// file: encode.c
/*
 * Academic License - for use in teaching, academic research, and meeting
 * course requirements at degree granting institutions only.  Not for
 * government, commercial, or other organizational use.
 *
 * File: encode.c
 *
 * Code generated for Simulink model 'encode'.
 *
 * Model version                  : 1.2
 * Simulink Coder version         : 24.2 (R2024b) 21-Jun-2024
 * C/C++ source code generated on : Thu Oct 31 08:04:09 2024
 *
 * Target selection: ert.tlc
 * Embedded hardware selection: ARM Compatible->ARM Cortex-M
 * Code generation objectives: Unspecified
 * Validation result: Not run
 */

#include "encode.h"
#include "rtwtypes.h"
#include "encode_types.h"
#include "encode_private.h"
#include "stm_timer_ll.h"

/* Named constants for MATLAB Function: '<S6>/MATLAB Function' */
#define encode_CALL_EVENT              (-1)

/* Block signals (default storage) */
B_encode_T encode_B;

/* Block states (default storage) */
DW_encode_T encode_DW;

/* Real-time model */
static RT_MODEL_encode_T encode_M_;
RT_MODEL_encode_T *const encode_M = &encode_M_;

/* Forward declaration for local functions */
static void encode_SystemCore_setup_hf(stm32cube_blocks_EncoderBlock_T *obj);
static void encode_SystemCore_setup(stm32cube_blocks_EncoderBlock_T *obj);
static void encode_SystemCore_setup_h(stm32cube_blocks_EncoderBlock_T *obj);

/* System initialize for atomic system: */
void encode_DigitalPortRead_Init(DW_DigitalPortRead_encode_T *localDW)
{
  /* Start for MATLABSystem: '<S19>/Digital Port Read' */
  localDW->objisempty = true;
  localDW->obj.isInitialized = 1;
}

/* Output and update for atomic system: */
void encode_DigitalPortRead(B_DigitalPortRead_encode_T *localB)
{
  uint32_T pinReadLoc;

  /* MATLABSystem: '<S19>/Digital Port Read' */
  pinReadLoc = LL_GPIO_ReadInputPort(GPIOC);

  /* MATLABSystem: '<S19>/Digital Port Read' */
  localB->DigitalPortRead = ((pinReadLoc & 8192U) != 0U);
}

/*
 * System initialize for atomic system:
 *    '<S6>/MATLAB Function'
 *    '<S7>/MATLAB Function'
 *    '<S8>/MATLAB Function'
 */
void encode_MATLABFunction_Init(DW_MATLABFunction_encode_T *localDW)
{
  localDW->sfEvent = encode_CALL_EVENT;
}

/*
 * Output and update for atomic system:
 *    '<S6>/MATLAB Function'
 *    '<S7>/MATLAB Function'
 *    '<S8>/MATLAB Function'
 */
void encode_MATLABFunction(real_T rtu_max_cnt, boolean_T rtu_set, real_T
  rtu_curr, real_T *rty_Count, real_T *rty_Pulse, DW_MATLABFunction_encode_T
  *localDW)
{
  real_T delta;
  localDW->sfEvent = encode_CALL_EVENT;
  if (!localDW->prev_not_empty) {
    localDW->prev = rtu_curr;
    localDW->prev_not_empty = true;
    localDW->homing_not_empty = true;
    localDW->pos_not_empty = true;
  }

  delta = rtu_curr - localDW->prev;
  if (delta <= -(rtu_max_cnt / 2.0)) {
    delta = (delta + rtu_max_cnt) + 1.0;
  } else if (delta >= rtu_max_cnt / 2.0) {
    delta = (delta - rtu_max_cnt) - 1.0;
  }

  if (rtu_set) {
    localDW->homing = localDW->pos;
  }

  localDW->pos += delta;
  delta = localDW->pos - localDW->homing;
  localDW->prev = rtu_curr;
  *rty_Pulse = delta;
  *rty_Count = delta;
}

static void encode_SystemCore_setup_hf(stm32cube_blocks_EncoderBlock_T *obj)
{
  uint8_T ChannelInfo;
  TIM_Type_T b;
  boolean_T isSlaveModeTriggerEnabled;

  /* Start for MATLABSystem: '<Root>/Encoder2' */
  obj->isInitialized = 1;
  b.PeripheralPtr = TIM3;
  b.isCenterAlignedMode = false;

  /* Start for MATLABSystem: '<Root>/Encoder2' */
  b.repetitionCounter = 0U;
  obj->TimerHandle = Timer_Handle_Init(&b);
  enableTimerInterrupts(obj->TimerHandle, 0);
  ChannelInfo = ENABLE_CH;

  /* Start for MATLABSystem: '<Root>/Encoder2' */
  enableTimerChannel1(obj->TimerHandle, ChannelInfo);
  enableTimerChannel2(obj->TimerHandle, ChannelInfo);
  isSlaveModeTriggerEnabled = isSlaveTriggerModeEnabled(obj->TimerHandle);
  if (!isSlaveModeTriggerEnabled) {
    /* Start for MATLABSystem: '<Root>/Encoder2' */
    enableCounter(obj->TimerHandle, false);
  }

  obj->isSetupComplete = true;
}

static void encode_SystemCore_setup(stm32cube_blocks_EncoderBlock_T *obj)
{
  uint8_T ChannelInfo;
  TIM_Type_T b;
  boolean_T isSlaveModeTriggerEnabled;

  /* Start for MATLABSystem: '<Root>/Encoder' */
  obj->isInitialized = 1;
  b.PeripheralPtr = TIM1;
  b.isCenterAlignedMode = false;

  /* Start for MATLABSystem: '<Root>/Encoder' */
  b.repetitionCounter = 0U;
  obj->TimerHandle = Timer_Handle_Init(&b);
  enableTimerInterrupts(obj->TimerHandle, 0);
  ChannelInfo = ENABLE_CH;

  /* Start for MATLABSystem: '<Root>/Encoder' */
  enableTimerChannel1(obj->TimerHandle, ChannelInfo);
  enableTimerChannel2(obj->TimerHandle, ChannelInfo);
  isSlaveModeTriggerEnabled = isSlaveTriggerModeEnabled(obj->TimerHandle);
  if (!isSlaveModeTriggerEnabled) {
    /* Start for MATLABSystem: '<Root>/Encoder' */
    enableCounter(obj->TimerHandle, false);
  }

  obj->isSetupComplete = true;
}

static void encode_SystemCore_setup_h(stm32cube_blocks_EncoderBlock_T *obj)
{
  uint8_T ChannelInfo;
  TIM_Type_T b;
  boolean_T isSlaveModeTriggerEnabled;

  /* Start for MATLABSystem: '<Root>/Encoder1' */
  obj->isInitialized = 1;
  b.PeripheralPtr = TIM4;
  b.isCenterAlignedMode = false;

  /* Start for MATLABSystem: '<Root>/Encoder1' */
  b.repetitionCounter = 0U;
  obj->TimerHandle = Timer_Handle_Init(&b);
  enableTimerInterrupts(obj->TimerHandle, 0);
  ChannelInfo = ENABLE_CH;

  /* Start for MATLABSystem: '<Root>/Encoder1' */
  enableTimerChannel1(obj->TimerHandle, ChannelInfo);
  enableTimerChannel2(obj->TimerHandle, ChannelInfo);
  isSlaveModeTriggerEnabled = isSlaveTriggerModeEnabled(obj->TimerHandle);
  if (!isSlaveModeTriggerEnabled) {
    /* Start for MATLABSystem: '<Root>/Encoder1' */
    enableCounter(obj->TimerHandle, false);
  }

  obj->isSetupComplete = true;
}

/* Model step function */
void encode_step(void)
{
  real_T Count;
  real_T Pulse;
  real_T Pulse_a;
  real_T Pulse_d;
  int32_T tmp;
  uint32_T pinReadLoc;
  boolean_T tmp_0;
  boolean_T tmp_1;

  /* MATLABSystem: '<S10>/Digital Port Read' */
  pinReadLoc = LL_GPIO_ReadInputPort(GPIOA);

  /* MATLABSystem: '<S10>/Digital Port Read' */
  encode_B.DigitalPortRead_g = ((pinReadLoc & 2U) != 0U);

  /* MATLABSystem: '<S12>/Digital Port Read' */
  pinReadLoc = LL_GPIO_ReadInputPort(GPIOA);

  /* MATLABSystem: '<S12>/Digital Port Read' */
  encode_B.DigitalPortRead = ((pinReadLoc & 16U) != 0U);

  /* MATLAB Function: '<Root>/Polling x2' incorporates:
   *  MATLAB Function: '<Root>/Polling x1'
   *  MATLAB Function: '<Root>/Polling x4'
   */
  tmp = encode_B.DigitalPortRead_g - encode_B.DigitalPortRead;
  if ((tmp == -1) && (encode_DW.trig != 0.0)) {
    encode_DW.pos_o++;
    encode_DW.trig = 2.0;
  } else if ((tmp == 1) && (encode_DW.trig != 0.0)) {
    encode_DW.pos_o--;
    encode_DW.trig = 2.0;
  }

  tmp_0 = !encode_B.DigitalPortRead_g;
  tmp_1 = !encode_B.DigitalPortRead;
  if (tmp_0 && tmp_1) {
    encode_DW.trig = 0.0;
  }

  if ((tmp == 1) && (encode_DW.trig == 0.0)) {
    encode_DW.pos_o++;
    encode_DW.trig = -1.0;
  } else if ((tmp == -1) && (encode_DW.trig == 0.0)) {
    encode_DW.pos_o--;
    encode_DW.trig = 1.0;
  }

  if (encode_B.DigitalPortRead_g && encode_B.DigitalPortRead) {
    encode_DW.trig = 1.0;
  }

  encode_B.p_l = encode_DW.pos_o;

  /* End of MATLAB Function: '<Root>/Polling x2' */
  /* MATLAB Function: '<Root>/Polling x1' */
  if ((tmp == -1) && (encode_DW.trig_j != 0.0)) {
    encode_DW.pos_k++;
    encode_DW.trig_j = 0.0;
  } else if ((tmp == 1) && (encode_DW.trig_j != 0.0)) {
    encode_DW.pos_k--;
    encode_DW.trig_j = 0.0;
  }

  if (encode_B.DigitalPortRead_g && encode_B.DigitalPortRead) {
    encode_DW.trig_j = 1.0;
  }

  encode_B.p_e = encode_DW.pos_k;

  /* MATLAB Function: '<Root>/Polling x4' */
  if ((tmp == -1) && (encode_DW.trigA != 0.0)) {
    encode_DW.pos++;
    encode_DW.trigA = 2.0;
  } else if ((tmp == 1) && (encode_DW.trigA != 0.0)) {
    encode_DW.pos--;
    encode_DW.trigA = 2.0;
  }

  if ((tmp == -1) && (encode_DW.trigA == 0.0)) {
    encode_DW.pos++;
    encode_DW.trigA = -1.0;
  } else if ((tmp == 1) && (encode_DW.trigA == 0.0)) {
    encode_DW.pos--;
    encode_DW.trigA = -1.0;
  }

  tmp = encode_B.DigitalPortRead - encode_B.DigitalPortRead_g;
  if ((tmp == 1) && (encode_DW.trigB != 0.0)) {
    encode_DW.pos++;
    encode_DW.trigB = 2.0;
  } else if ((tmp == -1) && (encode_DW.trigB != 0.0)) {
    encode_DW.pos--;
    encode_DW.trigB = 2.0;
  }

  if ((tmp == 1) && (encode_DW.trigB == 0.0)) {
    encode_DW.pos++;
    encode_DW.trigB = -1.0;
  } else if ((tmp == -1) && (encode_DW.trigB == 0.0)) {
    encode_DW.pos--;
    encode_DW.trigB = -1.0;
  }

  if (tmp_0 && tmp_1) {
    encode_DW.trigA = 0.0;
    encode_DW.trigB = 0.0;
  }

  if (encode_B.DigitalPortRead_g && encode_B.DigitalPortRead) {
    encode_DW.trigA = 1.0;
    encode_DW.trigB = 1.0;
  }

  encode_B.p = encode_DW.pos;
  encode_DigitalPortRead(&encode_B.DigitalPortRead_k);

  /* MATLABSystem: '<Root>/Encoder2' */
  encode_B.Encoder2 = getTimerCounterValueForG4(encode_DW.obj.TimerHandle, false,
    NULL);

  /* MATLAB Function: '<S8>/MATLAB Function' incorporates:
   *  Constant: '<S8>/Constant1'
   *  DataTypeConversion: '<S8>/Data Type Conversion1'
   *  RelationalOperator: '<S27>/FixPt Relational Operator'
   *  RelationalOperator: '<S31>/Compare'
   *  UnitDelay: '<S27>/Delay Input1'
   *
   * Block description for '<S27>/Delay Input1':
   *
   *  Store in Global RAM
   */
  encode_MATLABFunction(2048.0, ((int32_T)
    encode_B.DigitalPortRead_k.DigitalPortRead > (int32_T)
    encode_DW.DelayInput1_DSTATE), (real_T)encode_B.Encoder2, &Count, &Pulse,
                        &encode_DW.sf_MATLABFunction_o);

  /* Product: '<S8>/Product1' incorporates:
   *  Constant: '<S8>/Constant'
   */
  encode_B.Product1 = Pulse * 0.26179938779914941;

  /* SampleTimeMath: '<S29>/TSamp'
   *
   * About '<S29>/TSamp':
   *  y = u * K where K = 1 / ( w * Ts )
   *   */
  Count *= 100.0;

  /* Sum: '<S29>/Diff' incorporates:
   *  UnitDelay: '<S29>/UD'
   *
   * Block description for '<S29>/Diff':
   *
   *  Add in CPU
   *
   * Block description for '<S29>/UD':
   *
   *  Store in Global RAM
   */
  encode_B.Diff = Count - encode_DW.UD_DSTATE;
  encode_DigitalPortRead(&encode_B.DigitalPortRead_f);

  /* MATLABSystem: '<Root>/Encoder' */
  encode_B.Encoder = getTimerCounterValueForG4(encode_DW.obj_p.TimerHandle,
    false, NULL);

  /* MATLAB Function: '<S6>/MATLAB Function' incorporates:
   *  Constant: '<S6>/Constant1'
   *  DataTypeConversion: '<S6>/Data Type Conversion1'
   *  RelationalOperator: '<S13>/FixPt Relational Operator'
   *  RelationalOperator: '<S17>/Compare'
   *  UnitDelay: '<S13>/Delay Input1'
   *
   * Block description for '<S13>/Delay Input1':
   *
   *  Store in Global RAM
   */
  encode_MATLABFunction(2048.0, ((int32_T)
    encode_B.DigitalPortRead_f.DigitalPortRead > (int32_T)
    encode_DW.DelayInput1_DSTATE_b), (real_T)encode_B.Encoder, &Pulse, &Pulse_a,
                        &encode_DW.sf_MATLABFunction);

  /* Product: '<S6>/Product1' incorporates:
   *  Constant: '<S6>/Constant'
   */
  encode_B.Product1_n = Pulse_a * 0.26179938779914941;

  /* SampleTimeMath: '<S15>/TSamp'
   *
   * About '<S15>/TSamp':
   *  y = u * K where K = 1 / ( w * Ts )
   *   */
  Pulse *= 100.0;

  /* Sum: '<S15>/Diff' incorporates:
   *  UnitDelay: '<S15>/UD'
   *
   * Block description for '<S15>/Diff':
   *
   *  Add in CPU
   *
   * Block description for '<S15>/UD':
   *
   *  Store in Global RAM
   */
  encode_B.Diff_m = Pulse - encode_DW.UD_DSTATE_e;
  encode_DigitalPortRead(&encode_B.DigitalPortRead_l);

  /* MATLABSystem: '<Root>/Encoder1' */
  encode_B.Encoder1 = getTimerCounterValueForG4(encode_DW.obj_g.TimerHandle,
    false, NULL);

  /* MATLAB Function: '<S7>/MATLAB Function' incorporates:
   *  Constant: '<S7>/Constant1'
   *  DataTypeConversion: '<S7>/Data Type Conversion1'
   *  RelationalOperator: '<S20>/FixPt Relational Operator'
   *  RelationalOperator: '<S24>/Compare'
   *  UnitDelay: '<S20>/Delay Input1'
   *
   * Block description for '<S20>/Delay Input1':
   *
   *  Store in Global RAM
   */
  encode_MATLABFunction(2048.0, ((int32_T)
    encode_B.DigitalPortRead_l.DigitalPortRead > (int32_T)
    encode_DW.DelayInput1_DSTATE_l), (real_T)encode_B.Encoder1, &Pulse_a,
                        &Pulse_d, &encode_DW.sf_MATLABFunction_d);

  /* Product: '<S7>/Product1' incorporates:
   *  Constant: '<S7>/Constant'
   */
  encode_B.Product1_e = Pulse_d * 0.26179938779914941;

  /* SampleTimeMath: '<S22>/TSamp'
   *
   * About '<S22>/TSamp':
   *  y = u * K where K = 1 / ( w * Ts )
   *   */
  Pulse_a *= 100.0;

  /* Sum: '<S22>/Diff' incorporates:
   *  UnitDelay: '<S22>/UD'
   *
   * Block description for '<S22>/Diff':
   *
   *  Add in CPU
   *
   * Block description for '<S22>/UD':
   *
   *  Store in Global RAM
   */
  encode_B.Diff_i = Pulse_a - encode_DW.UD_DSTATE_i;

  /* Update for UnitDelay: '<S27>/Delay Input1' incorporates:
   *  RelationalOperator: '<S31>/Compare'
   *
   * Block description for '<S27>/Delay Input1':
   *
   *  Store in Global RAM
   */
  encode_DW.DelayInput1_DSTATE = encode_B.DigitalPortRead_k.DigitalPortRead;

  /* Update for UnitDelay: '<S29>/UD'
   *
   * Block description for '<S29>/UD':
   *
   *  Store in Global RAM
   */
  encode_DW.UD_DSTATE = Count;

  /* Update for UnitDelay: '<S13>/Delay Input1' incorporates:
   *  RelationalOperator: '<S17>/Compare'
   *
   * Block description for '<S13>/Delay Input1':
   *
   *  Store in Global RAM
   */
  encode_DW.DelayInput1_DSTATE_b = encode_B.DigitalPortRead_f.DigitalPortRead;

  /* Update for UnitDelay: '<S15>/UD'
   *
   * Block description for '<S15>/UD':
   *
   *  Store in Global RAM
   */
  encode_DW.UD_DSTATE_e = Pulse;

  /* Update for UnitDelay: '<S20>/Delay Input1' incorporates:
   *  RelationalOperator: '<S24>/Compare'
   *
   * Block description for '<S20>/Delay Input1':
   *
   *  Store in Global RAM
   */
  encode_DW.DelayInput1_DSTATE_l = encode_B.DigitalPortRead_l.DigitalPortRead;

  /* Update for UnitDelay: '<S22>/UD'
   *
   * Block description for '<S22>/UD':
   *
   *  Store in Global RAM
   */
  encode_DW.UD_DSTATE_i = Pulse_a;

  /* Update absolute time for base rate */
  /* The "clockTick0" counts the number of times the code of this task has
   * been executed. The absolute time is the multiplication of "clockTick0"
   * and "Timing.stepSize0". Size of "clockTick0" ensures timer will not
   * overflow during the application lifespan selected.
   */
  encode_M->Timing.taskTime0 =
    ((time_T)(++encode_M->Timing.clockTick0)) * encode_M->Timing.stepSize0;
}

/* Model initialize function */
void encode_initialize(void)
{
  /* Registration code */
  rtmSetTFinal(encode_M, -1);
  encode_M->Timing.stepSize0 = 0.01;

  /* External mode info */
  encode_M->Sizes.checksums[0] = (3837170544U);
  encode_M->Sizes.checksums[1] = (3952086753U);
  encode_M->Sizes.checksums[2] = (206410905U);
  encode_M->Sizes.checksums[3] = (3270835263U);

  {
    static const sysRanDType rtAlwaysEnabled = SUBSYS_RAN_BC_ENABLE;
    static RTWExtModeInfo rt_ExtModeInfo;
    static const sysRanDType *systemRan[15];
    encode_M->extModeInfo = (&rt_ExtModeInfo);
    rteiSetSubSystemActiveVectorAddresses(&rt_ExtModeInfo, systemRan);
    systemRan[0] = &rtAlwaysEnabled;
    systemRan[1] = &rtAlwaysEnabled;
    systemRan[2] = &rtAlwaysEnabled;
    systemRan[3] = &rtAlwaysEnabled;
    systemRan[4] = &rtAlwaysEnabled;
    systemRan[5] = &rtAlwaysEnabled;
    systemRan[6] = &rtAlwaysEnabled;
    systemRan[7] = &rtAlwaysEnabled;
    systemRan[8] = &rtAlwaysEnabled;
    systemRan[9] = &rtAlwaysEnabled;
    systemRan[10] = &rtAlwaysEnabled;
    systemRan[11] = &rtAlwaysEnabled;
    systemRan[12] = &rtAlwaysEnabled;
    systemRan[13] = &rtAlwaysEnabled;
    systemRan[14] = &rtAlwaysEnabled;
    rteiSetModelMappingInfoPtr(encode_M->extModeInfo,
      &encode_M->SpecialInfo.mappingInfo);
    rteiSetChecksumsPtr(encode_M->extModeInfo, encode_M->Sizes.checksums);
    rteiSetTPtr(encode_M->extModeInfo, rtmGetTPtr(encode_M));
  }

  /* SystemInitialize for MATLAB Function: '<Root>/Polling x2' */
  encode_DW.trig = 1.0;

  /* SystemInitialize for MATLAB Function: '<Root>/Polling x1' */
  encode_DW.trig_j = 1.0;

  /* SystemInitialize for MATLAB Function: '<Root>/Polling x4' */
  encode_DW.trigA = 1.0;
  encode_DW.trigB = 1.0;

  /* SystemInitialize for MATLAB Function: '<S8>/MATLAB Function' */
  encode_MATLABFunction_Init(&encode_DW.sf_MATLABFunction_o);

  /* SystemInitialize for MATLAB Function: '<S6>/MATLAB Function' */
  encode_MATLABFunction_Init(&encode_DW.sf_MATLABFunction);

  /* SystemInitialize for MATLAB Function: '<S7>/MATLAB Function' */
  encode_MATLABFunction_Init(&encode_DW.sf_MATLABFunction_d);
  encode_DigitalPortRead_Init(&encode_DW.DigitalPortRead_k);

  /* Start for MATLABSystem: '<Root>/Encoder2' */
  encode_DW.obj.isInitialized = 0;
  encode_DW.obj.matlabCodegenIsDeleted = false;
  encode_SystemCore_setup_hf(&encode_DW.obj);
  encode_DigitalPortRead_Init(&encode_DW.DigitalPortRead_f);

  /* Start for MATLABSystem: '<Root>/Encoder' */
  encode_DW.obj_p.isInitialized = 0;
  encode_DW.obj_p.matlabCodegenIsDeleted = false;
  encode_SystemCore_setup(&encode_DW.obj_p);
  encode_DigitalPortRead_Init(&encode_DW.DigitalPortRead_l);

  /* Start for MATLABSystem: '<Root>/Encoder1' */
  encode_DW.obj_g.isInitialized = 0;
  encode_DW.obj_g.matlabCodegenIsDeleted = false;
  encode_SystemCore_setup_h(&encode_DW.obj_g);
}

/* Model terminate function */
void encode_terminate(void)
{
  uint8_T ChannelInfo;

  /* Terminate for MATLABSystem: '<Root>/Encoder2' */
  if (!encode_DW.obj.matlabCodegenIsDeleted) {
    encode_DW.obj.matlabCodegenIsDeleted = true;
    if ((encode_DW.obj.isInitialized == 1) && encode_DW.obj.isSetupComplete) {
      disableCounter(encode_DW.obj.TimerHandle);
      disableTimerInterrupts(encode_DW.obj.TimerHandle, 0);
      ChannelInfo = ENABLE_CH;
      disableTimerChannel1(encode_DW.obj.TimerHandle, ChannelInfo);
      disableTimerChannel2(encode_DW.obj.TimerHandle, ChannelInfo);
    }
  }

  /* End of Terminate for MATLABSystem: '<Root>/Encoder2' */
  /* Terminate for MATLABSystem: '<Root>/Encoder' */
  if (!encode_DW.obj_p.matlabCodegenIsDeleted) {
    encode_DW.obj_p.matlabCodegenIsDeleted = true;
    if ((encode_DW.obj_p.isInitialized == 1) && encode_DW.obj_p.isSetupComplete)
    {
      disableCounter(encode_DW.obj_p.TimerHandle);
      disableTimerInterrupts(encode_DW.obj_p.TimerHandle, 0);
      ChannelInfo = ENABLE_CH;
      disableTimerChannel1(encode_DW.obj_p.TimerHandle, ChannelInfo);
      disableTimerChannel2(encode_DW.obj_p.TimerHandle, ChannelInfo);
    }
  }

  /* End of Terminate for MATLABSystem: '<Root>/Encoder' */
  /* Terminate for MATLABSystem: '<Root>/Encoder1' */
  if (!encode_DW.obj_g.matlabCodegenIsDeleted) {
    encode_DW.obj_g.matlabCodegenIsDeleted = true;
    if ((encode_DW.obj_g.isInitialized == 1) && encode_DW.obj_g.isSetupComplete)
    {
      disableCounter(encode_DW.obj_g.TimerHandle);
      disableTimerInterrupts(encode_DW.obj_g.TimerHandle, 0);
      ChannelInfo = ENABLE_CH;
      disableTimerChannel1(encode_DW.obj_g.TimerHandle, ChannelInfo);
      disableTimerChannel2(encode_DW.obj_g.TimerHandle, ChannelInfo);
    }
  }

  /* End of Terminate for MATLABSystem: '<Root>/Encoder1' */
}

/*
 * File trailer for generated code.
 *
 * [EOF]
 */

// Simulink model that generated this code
simulink model "encode"  (R2024b)
settings: Solver=FixedStepAuto  StartTime=0.0  StopTime=inf  FixedStep=0.01  RelTol=1e-3  EnableMultiTasking=on
libraries: simulink x6, stm32f4xxblockslib x5, stm32g4xxblockslib x3

== system encode ==
  Display{1..4,6..7,9..10,12} (9 alike) : Display
  Encoder : stm32g4xxblockslib/Encoder  TimerModule=TIM1  EnableResetInput=off  OutputCountAfterFirstIndex=off  OutputValidIndex=off  OutputDirection=off  OutputStatus=off  SampleTime=-1
  Encoder1 : stm32g4xxblockslib/Encoder  TimerModule=TIM4  EnableResetInput=off  OutputCountAfterFirstIndex=off  OutputValidIndex=off  OutputDirection=off  OutputStatus=off  SampleTime=-1
  Encoder2 : stm32g4xxblockslib/Encoder  TimerModule=TIM3  EnableResetInput=off  OutputCountAfterFirstIndex=off  OutputValidIndex=off  OutputDirection=off  OutputStatus=off  SampleTime=-1
  PA1_ReadA : stm32f4xxblockslib/Digital Port Read  PortName=GPIOA  PinNumber=[1]  ReadOperation=on  IOAsArray=on  SampleTime=-1  EnableSimPort=off  hoistedMaskSrc=ECSoC/ECSimCodegen/Digital Port Read
  PA4_ReadB : stm32f4xxblockslib/Digital Port Read  PortName=GPIOA  PinNumber=[4]  ReadOperation=on  IOAsArray=on  SampleTime=-1  EnableSimPort=off  hoistedMaskSrc=ECSoC/ECSimCodegen/Digital Port Read
  Polling x1 : MATLAB Function  TreatAsAtomicUnit=on
  Polling x2 : MATLAB Function  TreatAsAtomicUnit=on
  Polling x4 : MATLAB Function  TreatAsAtomicUnit=on
  QEI x1 : Subsystem
  QEI x2 : Subsystem
  QEI x4 : Subsystem
  wires:
  PA4_ReadB/1 -> Polling x2/2(b), Polling x4/2(b), Polling x1/2(b)
  PA1_ReadA/1 -> Polling x4/1(a), Polling x2/1(a), Polling x1/1(a)
  Encoder/1 -> QEI x1/1(curr)
  QEI x1/1(Velocity) -> Display4/1
  QEI x1/2(Position) -> Display6/1
  QEI x2/2(Position) -> Display9/1
  QEI x2/1(Velocity) -> Display7/1
  Encoder1/1 -> QEI x2/1(curr)
  QEI x4/2(Position) -> Display12/1
  QEI x4/1(Velocity) -> Display10/1
  Encoder2/1 -> QEI x4/1(curr)
  Polling x1/1(p) -> Display2/1
  Polling x2/1(p) -> Display1/1
  Polling x4/1(p) -> Display3/1

== system encode/QEI x1 ==
  curr : Inport
  Constant : Constant  Value=pi/12
  Constant1 : Constant  Value=2048
  Data Type Conversion1 : DataTypeConversion  OutDataTypeStr=double  SaturateOnIntegerOverflow=off  RndMeth=Floor
  Detect Rise Positive : simulink/Logic and Bit Operations/Detect Rise Positive  vinit=0  OutDataTypeStr=boolean
  Digital Port Read : stm32f4xxblockslib/Digital Port Read  PortName=GPIOC  PinNumber=[13]  ReadOperation=on  IOAsArray=on  SampleTime=-1  EnableSimPort=off  hoistedMaskSrc=ECSoC/ECSimCodegen/Digital Port Read
  Discrete Derivative : simulink/Discrete/Discrete Derivative  gainval=1.0  ICPrevScaledInput=0.0  OutMin=[]  OutMax=[]  OutDataType=fixdt(1, 16)  OutScaling=2^-10  DoSatur=off
  MATLAB Function : MATLAB Function  TreatAsAtomicUnit=on
  Product1 : Product
  Velocity : Outport
  Position : Outport  Port=2
  wires:
  Digital Port Read/1 -> Detect Rise Positive/1
  Detect Rise Positive/1 -> MATLAB Function/2(set)
  Data Type Conversion1/1 -> MATLAB Function/3(curr)
  curr/1 -> Data Type Conversion1/1
  MATLAB Function/1(Count) -> Discrete Derivative/1
  Discrete Derivative/1 -> Velocity/1
  MATLAB Function/2(Pulse) -> Product1/1
  Constant/1 -> Product1/2
  Product1/1 -> Position/1
  Constant1/1 -> MATLAB Function/1(max_cnt)

== system encode/QEI x2 ==
  curr : Inport
  Constant : Constant  Value=pi/12
  Constant1 : Constant  Value=2048
  Data Type Conversion1 : DataTypeConversion  OutDataTypeStr=double  SaturateOnIntegerOverflow=off  RndMeth=Floor
  Detect Rise Positive : simulink/Logic and Bit Operations/Detect Rise Positive  vinit=0  OutDataTypeStr=boolean
  Digital Port Read : stm32f4xxblockslib/Digital Port Read  PortName=GPIOC  PinNumber=[13]  ReadOperation=on  IOAsArray=on  SampleTime=-1  EnableSimPort=off  hoistedMaskSrc=ECSoC/ECSimCodegen/Digital Port Read
  Discrete Derivative : simulink/Discrete/Discrete Derivative  gainval=1.0  ICPrevScaledInput=0.0  OutMin=[]  OutMax=[]  OutDataType=fixdt(1, 16)  OutScaling=2^-10  DoSatur=off
  MATLAB Function : MATLAB Function  TreatAsAtomicUnit=on
  Product1 : Product
  Velocity : Outport
  Position : Outport  Port=2
  wires:
  Digital Port Read/1 -> Detect Rise Positive/1
  Detect Rise Positive/1 -> MATLAB Function/2(set)
  Data Type Conversion1/1 -> MATLAB Function/3(curr)
  curr/1 -> Data Type Conversion1/1
  MATLAB Function/1(Count) -> Discrete Derivative/1
  Discrete Derivative/1 -> Velocity/1
  MATLAB Function/2(Pulse) -> Product1/1
  Constant/1 -> Product1/2
  Product1/1 -> Position/1
  Constant1/1 -> MATLAB Function/1(max_cnt)

== system encode/QEI x4 ==
  curr : Inport
  Constant : Constant  Value=pi/12
  Constant1 : Constant  Value=2048
  Data Type Conversion1 : DataTypeConversion  OutDataTypeStr=double  SaturateOnIntegerOverflow=off  RndMeth=Floor
  Detect Rise Positive : simulink/Logic and Bit Operations/Detect Rise Positive  vinit=0  OutDataTypeStr=boolean
  Digital Port Read : stm32f4xxblockslib/Digital Port Read  PortName=GPIOC  PinNumber=[13]  ReadOperation=on  IOAsArray=on  SampleTime=-1  EnableSimPort=off  hoistedMaskSrc=ECSoC/ECSimCodegen/Digital Port Read
  Discrete Derivative : simulink/Discrete/Discrete Derivative  gainval=1.0  ICPrevScaledInput=0.0  OutMin=[]  OutMax=[]  OutDataType=fixdt(1, 16)  OutScaling=2^-10  DoSatur=off
  MATLAB Function : MATLAB Function  TreatAsAtomicUnit=on
  Product1 : Product
  Velocity : Outport
  Position : Outport  Port=2
  wires:
  Digital Port Read/1 -> Detect Rise Positive/1
  Detect Rise Positive/1 -> MATLAB Function/2(set)
  Data Type Conversion1/1 -> MATLAB Function/3(curr)
  curr/1 -> Data Type Conversion1/1
  MATLAB Function/1(Count) -> Discrete Derivative/1
  Discrete Derivative/1 -> Velocity/1
  MATLAB Function/2(Pulse) -> Product1/1
  Constant/1 -> Product1/2
  Product1/1 -> Position/1
  Constant1/1 -> MATLAB Function/1(max_cnt)

== matlab function encode/Polling x2 ==
function p = fcn(a,b)
    persistent pos;
    persistent trig;
    if isempty(trig)
        trig = 1;
        pos = 0;
    end
    if a-b == -1 && trig
        pos = pos + 1;
        trig = 2;
    elseif a-b == 1 && trig
        pos = pos -1;
        trig = 2;
    end

    if a == 0 && b == 0 
        trig = 0;
    end

    if a-b == 1 && trig == 0
        pos = pos + 1;
        trig = -1;
    elseif a-b == -1 && trig == 0
        pos = pos -1;
        trig = 1;
    end

    if a == 1 && b == 1
        trig = 1;
    end
    p = pos;
end

== matlab function encode/Polling x1 ==
function p = fcn(a,b)
    persistent pos;
    persistent trig;
    if isempty(trig)
        trig = 1;
        pos = 0;
    end
    if a-b == -1 && trig
        pos = pos + 1;
        trig = 0;
    elseif a-b == 1 && trig
        pos = pos -1;
        trig = 0;
    end

    if a == 1 && b == 1
        trig = 1;
    end
    p = pos;
end

== matlab function encode/Polling x4 ==
function p = fcn(a,b)
    persistent pos;
    persistent trigA;
    persistent trigB;
    if isempty(trigA)
        trigA = 1;
        trigB = 1;
        pos = 0;
    end
    if a-b == -1 && trigA
        pos = pos + 1;
        trigA = 2;
    elseif a-b == 1 && trigA
        pos = pos -1;
        trigA = 2;
    end

    if a-b == -1 && trigA == 0
        pos = pos + 1;
        trigA = -1;
    elseif a-b == 1 && trigA == 0
        pos = pos -1;
        trigA = -1;
    end

    if b-a == 1 && trigB
        pos = pos + 1;
        trigB = 2;
    elseif b-a == -1 && trigB
        pos = pos - 1;
        trigB = 2;
    end

    if b-a == 1 && trigB == 0
        pos = pos + 1;
        trigB = -1;
    elseif b-a == -1 && trigB == 0
        pos = pos - 1;
        trigB = -1;
    end

    if a == 0 && b == 0
        trigA = 0;
        trigB = 0;
    end

    if a == 1 && b == 1
        trigA = 1;
        trigB = 1;
    end
    p = pos;
end

== matlab function encode/QEI x1/MATLAB Function ==
function [Count,Pulse] = fcn(max_cnt,set,curr)
    persistent prev;
    persistent homing;
    persistent pos;

    if isempty(prev)
        prev = curr;
        homing = 0;
        pos = 0;
    end

    delta = curr - prev;

    if delta <= -1*(max_cnt/2)
        delta = delta + max_cnt + 1;
    elseif delta >= max_cnt/2
        delta = delta -max_cnt - 1;
    end

    if set
        homing = pos;
    end

    pos = pos + delta;
    Count = pos - homing;
    prev = curr;

    Pulse = Count;

end

== matlab function encode/QEI x2/MATLAB Function ==
function [Count,Pulse] = fcn(max_cnt,set,curr)
    persistent prev;
    persistent homing;
    persistent pos;

    if isempty(prev)
        prev = curr;
        homing = 0;
        pos = 0;
    end

    delta = curr - prev;

    if delta <= -1*(max_cnt/2)
        delta = delta + max_cnt + 1;
    elseif delta >= max_cnt/2
        delta = delta -max_cnt - 1;
    end

    if set
        homing = pos;
    end

    pos = pos + delta;
    Count = pos - homing;
    prev = curr;

    Pulse = Count;

end

== matlab function encode/QEI x4/MATLAB Function ==
function [Count,Pulse] = fcn(max_cnt,set,curr)
    persistent prev;
    persistent homing;
    persistent pos;

    if isempty(prev)
        prev = curr;
        homing = 0;
        pos = 0;
    end

    delta = curr - prev;

    if delta <= -1*(max_cnt/2)
        delta = delta + max_cnt + 1;
    elseif delta >= max_cnt/2
        delta = delta -max_cnt - 1;
    end

    if set
        homing = pos;
    end

    pos = pos + delta;
    Count = pos - homing;
    prev = curr;

    Pulse = Count;

end
